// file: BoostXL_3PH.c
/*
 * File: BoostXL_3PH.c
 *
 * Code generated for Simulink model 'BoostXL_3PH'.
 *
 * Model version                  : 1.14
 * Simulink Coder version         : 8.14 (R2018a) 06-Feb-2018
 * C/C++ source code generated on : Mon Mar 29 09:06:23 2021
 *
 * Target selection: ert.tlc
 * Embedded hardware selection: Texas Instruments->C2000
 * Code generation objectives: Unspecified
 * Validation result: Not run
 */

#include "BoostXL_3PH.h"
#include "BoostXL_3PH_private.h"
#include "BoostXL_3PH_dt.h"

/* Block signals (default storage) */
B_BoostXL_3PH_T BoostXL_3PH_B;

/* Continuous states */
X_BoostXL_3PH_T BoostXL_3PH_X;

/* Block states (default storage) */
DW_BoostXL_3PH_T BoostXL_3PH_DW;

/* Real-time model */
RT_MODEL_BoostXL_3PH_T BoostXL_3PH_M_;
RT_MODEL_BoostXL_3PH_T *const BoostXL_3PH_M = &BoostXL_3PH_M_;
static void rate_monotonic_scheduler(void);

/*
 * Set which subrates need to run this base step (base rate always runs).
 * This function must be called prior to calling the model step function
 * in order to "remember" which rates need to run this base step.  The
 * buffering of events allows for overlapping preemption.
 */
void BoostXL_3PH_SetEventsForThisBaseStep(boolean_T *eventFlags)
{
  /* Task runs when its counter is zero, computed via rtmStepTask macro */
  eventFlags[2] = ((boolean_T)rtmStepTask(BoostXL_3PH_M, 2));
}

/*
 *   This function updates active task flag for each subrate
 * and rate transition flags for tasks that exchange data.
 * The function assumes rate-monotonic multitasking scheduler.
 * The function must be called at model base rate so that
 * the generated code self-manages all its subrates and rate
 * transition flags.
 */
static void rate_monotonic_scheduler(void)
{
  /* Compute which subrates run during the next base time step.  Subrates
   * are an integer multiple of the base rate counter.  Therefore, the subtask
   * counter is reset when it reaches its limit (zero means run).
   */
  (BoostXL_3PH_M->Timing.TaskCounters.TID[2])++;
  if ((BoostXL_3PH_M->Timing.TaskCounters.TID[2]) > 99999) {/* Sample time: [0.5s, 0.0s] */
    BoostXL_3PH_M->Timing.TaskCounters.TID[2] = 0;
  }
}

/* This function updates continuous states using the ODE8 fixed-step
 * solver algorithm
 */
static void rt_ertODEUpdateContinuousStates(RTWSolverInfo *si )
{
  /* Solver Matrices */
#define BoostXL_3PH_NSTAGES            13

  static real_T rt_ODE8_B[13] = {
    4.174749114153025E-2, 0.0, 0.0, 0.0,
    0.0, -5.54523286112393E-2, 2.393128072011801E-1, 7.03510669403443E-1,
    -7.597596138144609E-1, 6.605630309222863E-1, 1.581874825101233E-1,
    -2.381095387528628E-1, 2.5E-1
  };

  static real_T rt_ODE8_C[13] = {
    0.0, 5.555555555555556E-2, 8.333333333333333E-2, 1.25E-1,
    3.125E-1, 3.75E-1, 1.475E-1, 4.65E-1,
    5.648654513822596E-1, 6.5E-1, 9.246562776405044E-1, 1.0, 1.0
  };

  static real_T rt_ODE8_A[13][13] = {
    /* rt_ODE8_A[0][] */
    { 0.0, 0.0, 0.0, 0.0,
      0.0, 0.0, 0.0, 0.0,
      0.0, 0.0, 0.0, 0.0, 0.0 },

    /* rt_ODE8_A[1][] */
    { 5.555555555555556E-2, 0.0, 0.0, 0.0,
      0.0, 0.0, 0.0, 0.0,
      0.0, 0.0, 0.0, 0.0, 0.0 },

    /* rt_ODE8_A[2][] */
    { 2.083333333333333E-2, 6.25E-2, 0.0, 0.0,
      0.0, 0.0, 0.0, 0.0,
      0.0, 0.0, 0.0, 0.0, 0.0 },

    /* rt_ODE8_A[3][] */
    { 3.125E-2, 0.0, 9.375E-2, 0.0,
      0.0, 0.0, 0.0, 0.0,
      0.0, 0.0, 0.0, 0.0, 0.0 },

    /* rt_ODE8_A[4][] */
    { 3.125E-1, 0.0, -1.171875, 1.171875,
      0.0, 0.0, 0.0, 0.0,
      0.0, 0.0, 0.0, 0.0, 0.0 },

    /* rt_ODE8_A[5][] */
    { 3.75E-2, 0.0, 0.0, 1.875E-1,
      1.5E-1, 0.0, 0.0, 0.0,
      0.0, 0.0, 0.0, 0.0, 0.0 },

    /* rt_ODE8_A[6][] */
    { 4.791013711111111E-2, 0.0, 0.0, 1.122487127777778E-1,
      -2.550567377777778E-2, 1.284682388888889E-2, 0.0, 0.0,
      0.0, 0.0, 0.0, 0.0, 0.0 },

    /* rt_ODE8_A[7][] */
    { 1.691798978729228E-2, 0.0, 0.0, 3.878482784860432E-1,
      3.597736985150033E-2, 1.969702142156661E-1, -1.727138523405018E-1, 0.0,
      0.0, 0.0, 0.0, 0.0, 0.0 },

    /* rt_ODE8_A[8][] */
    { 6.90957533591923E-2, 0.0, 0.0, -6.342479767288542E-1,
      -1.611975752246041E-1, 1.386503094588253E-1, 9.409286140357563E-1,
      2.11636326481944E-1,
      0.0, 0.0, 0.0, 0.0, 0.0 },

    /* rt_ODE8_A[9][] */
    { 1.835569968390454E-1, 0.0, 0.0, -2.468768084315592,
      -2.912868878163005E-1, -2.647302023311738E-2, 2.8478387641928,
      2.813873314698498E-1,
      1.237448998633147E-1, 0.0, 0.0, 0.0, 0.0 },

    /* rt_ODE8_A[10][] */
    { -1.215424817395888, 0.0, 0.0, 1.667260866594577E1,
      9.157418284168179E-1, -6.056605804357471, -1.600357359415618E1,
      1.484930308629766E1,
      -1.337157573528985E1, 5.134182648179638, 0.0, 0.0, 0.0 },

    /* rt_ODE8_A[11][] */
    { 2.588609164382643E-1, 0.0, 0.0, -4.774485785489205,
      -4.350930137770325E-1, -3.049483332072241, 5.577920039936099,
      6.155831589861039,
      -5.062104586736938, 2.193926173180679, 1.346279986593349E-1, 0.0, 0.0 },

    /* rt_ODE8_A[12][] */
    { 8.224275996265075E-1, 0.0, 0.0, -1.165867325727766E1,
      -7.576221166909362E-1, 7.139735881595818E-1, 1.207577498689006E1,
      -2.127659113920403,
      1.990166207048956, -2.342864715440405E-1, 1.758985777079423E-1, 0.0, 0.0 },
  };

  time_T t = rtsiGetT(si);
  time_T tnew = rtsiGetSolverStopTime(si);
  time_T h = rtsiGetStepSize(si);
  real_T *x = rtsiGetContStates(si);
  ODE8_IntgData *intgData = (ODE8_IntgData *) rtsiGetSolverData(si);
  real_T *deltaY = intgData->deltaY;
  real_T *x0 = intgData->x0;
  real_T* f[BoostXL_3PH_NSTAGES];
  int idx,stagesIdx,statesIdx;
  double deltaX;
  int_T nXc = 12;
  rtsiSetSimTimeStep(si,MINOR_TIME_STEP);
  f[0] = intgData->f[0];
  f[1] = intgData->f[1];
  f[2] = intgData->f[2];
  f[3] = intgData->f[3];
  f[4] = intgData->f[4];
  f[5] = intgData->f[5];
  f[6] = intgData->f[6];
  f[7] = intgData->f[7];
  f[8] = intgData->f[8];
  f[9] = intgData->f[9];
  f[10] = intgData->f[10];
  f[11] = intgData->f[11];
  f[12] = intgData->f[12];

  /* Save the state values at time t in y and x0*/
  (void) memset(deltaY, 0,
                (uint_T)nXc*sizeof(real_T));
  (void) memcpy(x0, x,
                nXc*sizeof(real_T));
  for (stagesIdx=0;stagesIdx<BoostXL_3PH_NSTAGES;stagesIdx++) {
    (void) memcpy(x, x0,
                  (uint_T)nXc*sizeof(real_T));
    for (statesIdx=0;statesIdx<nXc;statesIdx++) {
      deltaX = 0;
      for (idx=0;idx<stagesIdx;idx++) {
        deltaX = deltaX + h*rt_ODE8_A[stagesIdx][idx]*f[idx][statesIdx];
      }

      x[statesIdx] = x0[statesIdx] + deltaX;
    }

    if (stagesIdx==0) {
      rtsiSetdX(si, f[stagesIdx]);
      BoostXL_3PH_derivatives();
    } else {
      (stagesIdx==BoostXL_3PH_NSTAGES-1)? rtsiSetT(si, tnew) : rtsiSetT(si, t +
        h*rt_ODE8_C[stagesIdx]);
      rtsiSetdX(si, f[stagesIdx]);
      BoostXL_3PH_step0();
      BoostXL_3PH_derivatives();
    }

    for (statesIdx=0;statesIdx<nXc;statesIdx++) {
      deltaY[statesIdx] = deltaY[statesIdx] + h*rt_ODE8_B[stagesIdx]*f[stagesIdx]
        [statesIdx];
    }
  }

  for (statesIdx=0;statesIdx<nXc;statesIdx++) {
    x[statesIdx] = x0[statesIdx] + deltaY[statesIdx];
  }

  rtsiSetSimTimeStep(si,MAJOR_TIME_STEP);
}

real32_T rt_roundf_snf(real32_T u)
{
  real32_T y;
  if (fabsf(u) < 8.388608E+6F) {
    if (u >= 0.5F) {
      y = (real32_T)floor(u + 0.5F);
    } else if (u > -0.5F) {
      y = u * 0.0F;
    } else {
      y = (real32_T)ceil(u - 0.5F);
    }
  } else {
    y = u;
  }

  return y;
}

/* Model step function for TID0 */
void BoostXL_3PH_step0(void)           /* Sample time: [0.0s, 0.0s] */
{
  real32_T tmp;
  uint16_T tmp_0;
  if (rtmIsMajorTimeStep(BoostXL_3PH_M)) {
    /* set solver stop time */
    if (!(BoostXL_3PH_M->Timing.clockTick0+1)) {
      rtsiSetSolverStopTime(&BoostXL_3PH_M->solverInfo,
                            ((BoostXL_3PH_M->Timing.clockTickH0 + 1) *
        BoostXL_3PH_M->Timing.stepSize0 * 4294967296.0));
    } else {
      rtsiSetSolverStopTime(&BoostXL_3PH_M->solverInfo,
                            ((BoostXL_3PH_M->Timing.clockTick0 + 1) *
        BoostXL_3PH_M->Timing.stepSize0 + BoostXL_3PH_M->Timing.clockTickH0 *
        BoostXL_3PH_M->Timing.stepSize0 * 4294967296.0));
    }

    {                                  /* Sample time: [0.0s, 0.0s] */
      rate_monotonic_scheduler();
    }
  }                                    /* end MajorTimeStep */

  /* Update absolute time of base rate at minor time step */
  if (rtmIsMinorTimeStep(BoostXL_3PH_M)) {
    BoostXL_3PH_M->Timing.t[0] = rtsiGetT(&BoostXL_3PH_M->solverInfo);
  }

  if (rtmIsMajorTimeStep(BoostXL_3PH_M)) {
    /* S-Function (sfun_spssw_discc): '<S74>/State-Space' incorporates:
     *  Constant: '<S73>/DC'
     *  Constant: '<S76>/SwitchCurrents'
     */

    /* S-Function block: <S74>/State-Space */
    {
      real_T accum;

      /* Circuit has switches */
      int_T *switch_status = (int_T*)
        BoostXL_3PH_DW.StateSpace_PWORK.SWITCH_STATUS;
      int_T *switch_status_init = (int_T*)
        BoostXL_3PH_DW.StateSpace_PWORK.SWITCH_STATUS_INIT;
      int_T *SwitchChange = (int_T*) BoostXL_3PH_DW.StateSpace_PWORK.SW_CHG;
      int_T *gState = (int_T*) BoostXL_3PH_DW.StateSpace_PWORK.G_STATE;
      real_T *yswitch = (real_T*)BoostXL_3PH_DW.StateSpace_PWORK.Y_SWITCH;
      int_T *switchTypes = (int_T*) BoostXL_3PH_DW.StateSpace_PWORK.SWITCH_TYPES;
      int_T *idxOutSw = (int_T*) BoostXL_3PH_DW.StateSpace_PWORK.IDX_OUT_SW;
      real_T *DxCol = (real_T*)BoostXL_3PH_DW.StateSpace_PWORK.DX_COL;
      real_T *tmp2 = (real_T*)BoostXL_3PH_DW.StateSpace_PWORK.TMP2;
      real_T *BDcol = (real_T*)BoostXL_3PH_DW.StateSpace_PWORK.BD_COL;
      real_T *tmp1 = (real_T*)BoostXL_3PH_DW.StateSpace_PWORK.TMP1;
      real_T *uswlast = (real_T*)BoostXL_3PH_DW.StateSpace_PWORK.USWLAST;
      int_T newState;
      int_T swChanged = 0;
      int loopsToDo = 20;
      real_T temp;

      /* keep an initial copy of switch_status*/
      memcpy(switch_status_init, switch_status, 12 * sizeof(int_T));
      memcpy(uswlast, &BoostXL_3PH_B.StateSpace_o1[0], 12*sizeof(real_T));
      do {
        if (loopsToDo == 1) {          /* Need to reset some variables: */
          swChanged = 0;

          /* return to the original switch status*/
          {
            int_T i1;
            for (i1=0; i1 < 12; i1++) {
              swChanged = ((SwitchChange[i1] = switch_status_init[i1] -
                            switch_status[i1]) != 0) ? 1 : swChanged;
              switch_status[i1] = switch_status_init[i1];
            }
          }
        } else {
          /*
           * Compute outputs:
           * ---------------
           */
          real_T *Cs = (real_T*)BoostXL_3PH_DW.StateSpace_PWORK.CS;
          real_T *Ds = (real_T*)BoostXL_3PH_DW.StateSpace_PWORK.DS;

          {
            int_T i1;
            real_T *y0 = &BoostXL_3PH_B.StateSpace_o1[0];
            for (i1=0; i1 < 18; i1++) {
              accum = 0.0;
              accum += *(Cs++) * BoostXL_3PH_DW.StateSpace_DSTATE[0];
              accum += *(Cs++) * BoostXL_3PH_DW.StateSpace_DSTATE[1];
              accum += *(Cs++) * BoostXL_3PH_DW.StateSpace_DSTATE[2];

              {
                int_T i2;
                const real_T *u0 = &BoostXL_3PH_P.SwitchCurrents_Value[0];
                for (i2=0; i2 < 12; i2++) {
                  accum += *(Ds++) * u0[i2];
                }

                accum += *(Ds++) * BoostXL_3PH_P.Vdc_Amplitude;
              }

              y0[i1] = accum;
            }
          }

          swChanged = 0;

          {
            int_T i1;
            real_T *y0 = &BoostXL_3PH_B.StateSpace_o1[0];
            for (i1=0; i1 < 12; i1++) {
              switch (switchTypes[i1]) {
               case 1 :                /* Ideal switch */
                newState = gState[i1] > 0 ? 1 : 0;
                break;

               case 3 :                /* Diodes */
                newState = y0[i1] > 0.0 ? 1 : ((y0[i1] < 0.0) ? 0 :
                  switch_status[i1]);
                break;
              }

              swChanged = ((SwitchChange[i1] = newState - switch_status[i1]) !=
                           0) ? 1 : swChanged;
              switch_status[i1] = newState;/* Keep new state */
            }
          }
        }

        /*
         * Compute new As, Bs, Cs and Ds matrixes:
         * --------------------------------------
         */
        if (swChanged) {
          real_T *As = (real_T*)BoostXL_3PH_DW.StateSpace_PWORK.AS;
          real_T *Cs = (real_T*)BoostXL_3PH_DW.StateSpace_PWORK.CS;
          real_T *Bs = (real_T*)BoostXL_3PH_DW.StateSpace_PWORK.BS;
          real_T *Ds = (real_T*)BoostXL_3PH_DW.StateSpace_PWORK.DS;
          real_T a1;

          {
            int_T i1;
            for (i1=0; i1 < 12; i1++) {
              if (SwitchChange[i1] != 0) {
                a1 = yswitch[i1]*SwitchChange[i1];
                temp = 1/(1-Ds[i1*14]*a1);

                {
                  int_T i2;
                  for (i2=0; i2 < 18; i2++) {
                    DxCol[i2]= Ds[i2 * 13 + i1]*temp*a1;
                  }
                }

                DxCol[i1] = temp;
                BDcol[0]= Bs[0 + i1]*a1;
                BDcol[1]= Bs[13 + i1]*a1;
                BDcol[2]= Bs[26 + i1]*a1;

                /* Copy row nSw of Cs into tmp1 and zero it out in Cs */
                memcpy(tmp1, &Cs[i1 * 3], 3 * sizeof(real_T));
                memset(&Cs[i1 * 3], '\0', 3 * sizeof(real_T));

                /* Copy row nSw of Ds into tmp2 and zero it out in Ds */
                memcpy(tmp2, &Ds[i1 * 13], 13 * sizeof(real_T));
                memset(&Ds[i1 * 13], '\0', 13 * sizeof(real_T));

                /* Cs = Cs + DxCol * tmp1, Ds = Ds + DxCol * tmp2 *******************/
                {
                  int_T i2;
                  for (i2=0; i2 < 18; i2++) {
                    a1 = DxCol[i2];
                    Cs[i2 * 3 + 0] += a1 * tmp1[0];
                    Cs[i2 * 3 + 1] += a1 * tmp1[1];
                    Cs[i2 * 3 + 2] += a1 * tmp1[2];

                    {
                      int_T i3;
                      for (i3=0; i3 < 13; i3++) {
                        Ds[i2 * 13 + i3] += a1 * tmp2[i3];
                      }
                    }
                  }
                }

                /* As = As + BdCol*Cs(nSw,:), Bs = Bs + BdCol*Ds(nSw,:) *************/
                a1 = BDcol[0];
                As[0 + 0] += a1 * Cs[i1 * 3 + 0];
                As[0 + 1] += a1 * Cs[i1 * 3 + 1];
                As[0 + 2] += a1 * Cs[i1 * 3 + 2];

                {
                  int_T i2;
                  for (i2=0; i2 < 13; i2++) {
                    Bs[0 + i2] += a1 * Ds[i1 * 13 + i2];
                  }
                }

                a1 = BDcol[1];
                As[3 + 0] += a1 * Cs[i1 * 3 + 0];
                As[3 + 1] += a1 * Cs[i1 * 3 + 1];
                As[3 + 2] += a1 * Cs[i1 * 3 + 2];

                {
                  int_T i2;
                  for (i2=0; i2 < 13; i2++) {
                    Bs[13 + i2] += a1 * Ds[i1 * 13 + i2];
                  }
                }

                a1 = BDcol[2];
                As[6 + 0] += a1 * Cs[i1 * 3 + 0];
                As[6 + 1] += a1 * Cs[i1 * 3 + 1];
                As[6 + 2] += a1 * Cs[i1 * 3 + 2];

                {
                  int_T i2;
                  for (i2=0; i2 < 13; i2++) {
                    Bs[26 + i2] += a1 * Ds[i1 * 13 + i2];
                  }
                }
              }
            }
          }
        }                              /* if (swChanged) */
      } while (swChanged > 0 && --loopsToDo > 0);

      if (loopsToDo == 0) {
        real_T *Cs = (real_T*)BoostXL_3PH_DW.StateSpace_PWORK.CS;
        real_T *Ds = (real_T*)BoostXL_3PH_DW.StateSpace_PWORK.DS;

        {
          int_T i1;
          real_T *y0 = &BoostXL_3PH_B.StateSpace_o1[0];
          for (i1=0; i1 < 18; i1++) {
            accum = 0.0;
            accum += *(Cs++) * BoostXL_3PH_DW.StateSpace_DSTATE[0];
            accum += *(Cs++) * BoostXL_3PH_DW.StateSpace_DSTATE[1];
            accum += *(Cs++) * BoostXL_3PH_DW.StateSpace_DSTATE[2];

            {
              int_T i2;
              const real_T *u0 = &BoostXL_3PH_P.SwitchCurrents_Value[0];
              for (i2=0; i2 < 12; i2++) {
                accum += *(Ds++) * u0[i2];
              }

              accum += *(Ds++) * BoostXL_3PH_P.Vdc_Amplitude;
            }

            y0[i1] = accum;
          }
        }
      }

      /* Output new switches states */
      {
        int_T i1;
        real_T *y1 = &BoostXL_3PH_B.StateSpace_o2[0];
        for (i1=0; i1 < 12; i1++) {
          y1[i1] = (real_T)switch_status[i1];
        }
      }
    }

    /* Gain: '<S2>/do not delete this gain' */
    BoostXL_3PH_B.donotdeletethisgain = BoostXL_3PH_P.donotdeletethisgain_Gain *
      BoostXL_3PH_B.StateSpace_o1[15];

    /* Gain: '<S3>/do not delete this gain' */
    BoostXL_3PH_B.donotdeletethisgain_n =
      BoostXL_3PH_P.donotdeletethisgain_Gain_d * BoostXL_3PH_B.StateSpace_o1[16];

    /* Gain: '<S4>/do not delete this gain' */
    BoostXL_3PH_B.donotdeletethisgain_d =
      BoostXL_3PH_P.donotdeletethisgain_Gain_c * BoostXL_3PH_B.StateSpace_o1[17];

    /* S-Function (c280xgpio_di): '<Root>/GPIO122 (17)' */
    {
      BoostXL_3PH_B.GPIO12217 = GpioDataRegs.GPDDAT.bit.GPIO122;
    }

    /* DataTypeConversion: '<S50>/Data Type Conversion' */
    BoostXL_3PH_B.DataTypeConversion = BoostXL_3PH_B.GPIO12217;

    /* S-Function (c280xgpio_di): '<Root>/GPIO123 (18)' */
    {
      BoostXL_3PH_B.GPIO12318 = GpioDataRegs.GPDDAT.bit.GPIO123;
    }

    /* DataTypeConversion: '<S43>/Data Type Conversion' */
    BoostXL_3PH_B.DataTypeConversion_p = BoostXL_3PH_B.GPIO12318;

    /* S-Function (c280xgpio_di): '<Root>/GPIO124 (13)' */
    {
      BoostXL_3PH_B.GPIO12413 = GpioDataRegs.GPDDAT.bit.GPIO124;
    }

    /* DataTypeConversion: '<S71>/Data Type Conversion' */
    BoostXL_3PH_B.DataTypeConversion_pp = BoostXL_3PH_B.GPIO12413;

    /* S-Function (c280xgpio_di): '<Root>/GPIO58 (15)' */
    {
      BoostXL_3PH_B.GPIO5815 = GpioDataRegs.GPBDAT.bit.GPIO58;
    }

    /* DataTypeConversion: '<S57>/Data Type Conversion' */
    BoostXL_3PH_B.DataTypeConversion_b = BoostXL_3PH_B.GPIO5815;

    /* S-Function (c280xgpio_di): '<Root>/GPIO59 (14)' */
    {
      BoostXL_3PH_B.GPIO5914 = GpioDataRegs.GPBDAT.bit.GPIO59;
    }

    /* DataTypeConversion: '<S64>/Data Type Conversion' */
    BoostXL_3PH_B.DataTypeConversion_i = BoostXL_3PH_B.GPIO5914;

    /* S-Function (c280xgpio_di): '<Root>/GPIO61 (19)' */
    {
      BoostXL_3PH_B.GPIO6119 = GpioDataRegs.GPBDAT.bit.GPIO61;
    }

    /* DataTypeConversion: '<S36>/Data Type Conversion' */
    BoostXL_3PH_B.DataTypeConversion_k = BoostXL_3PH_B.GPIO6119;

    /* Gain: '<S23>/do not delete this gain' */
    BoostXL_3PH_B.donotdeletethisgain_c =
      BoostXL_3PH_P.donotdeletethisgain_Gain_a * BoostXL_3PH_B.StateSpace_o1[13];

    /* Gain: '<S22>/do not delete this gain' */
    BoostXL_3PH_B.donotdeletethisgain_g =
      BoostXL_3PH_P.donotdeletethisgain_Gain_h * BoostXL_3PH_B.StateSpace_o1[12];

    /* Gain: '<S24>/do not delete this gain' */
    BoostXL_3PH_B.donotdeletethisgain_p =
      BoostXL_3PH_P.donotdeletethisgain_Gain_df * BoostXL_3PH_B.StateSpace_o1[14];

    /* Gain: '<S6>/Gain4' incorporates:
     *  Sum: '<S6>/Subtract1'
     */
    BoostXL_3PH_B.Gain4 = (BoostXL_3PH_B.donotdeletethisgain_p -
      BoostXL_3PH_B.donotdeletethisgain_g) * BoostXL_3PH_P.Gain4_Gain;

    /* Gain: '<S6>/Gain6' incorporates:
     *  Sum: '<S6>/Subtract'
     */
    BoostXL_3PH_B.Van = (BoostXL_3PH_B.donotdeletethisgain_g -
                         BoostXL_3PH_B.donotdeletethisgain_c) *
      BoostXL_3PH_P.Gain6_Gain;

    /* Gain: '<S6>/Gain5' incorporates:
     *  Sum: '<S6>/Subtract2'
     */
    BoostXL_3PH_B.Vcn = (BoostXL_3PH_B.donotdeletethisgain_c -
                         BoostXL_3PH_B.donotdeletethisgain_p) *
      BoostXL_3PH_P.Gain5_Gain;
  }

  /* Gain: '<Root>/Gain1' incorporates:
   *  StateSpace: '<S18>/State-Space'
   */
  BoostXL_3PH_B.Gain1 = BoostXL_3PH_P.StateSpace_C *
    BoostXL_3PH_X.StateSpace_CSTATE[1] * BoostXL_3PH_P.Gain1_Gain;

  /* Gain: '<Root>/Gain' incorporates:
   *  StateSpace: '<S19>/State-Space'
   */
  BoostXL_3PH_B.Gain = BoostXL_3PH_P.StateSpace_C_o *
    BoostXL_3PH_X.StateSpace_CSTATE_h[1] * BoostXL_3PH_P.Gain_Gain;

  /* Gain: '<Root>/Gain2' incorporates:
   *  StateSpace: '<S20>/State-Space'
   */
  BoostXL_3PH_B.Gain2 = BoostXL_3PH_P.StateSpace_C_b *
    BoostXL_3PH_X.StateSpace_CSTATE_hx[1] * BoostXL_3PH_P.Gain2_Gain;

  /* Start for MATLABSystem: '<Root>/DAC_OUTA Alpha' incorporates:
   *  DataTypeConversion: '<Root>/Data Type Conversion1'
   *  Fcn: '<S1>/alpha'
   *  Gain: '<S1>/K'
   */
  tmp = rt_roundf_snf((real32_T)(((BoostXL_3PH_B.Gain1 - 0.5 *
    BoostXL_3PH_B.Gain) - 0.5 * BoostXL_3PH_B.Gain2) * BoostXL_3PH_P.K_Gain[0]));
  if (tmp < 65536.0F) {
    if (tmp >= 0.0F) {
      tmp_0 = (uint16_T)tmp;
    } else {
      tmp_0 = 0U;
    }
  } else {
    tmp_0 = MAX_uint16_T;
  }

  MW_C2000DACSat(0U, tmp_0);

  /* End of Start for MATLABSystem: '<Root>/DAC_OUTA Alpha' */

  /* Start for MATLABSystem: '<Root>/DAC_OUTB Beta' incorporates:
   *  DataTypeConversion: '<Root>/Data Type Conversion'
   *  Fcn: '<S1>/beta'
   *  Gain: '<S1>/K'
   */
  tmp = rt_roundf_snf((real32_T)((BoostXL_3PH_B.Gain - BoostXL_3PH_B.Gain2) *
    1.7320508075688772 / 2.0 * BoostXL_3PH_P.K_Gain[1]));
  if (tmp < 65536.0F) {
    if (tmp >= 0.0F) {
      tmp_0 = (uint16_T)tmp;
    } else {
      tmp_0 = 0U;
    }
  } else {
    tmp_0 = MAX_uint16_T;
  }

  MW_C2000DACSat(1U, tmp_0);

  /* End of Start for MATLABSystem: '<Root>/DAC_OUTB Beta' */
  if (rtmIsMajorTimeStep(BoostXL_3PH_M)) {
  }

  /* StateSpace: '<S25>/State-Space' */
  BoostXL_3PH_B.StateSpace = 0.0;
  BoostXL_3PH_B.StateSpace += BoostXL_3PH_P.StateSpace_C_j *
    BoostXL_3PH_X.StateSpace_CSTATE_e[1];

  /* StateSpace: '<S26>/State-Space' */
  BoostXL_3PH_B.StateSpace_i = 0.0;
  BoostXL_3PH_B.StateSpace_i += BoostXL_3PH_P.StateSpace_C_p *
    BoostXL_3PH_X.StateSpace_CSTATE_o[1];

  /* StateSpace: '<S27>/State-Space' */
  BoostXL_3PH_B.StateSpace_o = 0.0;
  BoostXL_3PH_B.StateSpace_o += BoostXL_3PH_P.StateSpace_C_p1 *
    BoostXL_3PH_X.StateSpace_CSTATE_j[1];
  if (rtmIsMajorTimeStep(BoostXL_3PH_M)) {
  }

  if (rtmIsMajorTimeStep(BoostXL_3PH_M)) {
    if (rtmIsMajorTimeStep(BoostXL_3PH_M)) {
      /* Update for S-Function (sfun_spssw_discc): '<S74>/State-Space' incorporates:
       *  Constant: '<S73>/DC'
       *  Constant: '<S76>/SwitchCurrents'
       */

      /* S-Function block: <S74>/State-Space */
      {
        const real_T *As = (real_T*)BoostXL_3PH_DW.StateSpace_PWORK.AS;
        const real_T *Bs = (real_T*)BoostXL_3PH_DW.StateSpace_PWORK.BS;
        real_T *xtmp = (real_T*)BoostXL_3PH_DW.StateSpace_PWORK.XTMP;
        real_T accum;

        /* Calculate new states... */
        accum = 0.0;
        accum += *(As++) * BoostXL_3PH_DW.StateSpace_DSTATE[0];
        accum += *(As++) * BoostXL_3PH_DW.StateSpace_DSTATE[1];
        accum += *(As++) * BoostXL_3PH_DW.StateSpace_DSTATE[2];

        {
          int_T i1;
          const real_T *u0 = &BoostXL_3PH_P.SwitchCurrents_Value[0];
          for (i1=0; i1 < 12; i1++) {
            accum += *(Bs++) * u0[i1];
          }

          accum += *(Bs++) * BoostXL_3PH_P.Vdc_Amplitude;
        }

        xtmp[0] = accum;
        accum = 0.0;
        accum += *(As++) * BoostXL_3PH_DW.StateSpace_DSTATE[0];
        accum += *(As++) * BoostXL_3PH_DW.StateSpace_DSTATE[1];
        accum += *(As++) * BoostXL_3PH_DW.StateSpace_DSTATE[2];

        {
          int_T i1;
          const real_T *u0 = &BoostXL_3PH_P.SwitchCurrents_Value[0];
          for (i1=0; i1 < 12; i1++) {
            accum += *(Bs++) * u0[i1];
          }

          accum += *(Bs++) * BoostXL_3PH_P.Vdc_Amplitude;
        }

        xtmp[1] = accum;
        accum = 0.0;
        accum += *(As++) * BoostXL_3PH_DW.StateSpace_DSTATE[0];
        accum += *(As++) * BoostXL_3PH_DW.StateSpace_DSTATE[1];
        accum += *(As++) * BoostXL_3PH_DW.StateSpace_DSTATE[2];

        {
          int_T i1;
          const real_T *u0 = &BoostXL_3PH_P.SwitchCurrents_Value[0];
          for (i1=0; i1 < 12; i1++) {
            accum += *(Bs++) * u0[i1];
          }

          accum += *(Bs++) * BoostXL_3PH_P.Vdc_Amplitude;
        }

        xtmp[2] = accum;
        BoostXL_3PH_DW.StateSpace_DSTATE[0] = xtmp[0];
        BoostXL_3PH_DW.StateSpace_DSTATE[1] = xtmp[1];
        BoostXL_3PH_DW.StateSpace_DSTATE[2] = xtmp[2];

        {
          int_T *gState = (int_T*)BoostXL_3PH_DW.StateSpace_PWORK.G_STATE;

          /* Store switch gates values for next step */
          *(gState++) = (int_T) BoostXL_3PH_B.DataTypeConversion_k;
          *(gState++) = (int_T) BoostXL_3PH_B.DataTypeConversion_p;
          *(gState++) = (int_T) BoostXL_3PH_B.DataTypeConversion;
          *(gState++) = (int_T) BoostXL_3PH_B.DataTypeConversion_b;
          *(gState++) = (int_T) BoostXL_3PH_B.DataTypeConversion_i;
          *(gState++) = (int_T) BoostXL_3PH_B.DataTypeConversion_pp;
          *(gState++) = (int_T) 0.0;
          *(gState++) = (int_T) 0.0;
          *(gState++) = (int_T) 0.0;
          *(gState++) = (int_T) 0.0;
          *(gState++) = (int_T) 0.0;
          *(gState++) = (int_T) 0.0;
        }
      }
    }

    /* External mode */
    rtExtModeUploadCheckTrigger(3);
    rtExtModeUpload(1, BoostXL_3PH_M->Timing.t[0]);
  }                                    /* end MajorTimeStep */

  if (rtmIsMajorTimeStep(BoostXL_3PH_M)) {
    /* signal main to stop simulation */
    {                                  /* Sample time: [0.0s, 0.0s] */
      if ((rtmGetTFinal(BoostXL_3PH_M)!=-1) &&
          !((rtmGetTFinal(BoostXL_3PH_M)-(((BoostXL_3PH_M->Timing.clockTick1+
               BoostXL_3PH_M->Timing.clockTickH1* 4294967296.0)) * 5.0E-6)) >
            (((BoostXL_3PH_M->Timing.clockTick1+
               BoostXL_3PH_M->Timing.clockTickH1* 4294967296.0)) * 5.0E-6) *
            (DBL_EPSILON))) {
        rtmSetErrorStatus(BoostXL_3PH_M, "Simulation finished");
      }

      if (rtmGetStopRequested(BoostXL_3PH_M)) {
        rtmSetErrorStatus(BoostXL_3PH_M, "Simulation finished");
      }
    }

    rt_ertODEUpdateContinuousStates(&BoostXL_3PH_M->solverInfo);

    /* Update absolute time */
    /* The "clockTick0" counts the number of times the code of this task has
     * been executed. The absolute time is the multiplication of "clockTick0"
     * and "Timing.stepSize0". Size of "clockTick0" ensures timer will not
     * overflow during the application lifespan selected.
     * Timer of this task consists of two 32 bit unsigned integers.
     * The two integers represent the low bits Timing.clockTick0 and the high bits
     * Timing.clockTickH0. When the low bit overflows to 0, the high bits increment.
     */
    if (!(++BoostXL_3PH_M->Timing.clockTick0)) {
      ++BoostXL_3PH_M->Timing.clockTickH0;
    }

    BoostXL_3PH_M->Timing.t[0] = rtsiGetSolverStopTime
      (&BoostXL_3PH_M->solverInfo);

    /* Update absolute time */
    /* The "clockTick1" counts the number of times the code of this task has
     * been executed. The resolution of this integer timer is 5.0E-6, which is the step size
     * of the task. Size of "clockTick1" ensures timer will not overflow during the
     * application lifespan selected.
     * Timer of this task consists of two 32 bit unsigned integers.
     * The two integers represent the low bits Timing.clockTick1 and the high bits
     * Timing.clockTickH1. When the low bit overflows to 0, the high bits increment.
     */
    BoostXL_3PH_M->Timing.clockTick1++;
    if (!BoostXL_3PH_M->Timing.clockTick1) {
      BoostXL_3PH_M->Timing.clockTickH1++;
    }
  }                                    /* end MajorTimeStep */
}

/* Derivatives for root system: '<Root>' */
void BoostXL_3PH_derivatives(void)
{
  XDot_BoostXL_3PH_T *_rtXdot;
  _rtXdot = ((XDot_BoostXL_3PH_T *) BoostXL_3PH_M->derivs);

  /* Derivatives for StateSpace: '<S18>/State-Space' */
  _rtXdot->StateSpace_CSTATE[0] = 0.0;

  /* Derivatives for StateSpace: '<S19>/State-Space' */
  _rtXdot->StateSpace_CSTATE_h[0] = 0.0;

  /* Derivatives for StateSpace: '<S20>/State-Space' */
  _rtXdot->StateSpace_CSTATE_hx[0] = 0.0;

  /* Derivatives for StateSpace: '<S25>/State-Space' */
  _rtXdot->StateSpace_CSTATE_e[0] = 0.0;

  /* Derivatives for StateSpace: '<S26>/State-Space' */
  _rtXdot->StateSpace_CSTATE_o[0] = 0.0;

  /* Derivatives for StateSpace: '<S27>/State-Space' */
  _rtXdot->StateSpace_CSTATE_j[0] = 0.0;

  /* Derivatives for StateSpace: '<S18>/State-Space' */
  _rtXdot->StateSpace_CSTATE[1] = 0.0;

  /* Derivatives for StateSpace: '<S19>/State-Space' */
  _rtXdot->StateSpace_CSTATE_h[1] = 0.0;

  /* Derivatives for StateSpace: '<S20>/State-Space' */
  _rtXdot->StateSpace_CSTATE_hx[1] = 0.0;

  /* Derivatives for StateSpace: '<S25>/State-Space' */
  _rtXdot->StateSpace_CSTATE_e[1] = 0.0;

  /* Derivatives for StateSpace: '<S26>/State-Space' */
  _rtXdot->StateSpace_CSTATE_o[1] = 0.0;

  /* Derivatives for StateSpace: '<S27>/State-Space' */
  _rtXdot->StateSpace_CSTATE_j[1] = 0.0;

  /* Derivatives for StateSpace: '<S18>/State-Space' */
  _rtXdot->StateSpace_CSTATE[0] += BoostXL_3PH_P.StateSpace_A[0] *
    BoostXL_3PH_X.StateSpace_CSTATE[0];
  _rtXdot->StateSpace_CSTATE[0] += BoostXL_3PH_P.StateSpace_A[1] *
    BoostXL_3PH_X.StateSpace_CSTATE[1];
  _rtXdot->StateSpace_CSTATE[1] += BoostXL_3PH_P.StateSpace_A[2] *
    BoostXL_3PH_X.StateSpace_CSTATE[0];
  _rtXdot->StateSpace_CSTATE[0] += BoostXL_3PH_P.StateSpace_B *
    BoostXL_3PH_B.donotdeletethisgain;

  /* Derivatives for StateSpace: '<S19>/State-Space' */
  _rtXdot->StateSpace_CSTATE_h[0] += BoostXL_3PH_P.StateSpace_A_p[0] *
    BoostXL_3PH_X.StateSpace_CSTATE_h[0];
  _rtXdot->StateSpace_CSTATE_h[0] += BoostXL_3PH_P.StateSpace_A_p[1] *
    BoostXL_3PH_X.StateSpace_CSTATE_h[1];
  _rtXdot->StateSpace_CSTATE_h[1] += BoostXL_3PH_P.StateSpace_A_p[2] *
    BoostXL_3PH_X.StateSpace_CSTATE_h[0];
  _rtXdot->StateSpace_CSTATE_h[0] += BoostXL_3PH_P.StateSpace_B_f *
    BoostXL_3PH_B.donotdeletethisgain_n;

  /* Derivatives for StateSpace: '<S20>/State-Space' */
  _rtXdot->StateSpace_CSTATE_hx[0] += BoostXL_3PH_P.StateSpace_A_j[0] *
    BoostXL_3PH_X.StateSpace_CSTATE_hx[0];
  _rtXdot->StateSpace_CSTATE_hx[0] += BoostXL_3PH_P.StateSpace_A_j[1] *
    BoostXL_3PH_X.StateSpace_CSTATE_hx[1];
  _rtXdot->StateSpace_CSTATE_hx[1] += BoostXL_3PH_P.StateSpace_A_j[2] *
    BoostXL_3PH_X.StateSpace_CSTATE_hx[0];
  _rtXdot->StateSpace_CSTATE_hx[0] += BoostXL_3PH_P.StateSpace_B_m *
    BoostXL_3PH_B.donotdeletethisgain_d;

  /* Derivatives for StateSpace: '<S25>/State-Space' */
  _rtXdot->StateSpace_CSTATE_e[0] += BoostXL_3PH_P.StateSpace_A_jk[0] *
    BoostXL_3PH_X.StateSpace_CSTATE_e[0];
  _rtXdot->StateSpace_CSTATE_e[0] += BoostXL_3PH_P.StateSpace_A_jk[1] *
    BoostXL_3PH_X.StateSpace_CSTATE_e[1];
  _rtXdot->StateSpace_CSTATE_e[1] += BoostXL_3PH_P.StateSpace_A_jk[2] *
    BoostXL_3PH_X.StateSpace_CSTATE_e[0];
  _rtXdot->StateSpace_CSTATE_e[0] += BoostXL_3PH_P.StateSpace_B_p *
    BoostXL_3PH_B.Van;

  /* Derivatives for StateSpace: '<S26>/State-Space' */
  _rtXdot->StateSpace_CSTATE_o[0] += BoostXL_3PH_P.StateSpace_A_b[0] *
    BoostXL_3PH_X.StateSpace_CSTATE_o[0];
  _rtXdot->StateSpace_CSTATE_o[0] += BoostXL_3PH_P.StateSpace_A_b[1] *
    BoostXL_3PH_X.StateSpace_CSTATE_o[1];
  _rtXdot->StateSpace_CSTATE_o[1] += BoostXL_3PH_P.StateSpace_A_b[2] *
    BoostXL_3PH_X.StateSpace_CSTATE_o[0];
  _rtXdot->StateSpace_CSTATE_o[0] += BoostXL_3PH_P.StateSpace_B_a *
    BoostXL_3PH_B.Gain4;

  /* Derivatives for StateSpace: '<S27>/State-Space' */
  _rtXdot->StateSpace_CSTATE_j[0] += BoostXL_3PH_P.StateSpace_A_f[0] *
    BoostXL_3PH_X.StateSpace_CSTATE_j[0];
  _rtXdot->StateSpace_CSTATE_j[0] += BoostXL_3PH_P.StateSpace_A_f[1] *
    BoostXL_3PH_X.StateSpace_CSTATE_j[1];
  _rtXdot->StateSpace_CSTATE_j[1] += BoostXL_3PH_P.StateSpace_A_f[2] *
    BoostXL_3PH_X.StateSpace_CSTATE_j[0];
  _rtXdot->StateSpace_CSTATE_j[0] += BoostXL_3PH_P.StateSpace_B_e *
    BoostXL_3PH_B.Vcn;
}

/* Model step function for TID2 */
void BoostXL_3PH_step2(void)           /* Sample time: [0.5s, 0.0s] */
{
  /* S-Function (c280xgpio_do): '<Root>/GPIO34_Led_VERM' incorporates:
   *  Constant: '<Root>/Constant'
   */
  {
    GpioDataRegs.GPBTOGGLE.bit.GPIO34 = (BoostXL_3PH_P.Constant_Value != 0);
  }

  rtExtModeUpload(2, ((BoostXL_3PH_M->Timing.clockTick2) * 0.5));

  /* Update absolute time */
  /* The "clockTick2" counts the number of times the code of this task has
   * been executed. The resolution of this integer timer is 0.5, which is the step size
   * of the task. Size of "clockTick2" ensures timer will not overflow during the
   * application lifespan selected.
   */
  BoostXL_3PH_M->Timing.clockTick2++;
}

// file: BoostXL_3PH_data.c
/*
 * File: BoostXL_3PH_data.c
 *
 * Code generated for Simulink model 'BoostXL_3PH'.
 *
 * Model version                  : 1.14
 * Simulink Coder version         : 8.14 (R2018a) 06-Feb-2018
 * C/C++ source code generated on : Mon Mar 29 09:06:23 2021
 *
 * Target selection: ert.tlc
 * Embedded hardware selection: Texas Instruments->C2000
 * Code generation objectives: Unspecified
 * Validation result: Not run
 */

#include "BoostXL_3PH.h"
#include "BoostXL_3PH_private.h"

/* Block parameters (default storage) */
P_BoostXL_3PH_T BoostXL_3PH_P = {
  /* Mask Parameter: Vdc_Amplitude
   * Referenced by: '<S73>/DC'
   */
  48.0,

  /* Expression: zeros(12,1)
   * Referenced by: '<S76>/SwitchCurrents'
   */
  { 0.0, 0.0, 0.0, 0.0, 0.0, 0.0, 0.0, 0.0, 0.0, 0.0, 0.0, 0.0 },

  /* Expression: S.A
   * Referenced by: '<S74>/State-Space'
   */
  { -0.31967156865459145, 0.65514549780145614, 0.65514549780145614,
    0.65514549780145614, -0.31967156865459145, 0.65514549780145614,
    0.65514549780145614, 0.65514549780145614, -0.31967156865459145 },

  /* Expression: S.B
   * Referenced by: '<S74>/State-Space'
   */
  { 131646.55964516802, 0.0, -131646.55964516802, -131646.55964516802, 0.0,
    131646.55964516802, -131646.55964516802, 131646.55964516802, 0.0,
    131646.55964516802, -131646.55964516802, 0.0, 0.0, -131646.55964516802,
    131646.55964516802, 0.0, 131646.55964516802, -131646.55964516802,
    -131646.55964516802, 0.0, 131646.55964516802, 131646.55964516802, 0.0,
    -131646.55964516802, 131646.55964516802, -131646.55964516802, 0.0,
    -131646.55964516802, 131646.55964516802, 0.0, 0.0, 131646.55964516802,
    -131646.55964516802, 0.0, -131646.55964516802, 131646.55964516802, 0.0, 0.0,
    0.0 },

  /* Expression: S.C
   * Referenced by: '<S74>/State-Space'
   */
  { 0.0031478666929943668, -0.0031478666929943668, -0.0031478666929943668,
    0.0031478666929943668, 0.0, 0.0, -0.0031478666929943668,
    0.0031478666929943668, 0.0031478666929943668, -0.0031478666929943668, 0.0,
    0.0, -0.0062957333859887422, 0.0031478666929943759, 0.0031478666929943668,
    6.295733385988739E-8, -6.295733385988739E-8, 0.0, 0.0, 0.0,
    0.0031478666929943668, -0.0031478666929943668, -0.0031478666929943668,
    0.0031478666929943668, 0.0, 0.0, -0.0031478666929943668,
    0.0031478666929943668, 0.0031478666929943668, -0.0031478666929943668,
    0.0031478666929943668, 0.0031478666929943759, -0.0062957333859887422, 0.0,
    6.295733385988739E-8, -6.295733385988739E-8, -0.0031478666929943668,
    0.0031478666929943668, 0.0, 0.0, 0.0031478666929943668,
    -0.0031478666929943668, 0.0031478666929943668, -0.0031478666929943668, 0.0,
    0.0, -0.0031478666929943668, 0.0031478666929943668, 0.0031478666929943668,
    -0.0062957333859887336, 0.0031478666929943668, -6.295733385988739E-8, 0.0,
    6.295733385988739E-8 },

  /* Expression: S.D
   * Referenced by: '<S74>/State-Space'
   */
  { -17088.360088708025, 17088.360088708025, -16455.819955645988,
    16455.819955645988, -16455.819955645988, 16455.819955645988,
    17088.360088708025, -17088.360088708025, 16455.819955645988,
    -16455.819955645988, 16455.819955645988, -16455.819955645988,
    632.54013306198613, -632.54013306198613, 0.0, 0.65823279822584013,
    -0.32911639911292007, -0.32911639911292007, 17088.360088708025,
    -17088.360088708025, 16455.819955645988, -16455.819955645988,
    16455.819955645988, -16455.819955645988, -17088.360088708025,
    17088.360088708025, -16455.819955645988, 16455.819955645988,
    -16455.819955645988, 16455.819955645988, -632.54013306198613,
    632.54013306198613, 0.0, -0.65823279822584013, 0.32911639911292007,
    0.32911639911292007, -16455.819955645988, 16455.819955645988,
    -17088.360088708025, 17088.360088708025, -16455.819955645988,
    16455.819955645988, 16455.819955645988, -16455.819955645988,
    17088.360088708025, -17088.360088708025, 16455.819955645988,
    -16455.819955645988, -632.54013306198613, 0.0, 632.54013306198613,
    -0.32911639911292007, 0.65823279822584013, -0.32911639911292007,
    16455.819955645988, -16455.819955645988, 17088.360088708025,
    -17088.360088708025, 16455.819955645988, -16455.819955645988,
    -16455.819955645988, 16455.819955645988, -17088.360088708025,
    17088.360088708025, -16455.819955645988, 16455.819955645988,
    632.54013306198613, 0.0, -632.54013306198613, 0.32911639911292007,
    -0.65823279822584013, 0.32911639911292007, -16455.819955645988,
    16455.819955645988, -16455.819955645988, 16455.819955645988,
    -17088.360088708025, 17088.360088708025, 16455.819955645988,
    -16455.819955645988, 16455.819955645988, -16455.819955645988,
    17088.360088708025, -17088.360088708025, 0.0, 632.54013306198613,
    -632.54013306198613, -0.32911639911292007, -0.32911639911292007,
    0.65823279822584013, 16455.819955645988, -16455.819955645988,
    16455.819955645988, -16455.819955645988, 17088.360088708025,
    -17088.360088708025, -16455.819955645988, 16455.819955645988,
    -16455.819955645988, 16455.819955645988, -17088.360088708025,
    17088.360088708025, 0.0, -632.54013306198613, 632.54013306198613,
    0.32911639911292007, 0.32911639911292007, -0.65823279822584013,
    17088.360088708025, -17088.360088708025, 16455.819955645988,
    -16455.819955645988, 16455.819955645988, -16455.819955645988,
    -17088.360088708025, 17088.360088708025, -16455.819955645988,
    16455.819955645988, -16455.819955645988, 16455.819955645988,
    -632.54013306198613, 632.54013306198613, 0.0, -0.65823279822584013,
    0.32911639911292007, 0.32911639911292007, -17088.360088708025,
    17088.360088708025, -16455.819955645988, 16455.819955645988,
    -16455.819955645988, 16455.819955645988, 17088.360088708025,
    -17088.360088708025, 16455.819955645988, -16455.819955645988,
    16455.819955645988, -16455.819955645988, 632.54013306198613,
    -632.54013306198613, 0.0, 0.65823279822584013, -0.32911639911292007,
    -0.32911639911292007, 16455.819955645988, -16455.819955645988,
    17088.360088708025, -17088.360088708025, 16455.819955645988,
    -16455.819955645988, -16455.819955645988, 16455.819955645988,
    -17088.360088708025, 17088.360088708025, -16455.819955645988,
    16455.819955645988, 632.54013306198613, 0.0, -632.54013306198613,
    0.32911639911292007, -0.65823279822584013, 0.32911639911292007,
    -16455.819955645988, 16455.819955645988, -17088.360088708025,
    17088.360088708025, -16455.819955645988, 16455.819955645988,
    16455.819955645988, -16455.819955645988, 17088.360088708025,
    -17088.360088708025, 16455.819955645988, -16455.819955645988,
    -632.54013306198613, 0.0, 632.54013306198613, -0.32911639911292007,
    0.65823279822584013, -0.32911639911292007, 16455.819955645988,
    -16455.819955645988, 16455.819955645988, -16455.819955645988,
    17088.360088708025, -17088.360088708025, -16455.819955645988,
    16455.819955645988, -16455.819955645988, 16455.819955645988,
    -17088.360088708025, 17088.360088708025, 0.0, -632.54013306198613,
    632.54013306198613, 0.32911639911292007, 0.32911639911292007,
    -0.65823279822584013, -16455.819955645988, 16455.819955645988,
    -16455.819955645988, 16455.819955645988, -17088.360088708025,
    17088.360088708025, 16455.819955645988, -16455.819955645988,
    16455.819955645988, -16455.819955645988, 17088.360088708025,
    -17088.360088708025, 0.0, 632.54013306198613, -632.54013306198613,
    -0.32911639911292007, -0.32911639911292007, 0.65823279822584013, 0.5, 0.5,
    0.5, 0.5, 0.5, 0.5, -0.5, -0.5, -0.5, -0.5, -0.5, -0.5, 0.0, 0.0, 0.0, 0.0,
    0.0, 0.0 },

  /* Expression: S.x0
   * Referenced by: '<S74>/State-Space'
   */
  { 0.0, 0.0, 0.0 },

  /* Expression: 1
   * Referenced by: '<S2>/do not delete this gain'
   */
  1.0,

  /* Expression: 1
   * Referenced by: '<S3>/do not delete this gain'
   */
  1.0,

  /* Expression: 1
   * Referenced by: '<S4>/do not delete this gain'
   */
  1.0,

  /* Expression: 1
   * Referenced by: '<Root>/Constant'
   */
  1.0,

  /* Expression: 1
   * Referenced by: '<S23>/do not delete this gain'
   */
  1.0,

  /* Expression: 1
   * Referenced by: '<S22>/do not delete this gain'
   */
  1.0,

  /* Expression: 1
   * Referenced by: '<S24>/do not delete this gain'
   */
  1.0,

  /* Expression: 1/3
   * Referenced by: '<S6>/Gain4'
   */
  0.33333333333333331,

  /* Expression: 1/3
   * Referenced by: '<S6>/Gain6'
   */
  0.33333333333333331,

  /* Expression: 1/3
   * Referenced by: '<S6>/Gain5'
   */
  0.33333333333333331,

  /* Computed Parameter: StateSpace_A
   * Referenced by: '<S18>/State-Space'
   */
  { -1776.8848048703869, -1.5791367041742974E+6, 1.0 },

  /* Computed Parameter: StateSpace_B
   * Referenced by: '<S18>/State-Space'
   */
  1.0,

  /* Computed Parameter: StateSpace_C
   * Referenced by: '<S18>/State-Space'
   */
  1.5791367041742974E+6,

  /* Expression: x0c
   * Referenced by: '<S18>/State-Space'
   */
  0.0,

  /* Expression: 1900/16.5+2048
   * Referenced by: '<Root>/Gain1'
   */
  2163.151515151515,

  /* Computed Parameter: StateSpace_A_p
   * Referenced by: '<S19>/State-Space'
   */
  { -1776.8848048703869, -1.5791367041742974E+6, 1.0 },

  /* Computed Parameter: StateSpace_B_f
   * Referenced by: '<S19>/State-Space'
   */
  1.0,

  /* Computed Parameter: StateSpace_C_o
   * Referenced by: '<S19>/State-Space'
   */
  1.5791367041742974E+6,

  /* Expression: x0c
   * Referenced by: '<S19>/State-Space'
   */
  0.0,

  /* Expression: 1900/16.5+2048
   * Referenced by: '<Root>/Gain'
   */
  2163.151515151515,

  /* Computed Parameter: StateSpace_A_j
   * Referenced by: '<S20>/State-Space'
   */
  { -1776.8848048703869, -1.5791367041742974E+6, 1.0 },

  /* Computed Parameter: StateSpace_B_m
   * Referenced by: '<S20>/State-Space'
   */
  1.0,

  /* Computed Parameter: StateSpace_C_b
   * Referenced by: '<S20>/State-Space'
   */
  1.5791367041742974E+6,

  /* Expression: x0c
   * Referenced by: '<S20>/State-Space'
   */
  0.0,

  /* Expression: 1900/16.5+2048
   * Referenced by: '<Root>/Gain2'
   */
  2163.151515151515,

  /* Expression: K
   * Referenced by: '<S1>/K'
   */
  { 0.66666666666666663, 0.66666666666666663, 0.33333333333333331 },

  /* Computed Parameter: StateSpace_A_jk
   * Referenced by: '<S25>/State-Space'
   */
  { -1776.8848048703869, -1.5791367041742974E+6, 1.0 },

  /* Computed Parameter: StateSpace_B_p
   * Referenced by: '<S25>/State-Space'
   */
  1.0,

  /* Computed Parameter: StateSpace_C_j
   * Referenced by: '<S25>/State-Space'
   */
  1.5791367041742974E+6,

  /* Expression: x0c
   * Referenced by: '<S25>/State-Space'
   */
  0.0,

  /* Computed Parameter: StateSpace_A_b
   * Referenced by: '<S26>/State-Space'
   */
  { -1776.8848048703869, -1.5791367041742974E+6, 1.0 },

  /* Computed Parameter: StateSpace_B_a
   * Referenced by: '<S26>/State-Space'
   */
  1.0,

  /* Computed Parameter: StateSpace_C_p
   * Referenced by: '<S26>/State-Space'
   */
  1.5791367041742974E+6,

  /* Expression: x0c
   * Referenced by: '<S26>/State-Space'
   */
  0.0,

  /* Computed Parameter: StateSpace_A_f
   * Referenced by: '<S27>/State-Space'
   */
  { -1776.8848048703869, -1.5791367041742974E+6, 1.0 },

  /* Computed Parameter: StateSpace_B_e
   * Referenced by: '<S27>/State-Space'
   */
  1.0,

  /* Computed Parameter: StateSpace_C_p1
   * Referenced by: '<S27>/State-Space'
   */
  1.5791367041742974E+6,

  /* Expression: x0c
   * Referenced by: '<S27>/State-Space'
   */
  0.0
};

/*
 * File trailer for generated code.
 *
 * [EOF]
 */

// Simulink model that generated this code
simulink model "BoostXL_3PH"  (R2018a)
settings: Solver=ode8  StartTime=0.0  StopTime=Inf  FixedStep=5e-6  MaxStep=5e-6  RelTol=1e-3  EnableMultiTasking=on
libraries: powerlib x15, c2837xDlib x9, powerlib_extras x6, peTransforms x1

== system BoostXL_3PH ==
  note: CONVERSOR TRIFÁSICO BOOSTXL
      | Victor Lopes
  Clarke Transform : peTransforms/Clarke Transform  PowerInvariant=off
  Constant : Constant  SampleTime=0.5
  Current Measueent1 : powerlib/Measurements/Current Measurement  PhasorSimulation=off  OutputType=Magnitude  PSBequivalent=0
  Current Measueent2 : powerlib/Measurements/Current Measurement  PhasorSimulation=off  OutputType=Magnitude  PSBequivalent=0
  Current Measueent3 : powerlib/Measurements/Current Measurement  PhasorSimulation=off  OutputType=Magnitude  PSBequivalent=0
  DAC_OUTA Alpha : c2837xDlib/DAC  channel=A  saturate=on
  DAC_OUTB Beta : c2837xDlib/DAC  channel=B  saturate=on
  Data Type Conversion : DataTypeConversion
  Data Type Conversion1 : DataTypeConversion
  Demux : Demux  Outputs=3
  GPIO122 (17) : c2837xDlib/Digital Input  GPIO_Number=GPIO120~GPIO127  GPIO_Bit0=off  GPIO_Bit1=off  GPIO_Bit2=on  GPIO_Bit3=off  GPIO_Bit4=off  GPIO_Bit5=off  GPIO_Bit6=off  GPIO_Bit7=off  sampleTime=-1  dataType=boolean  GPIO_Bit0_Qualification=Sync to SYSCLKOUT  GPIO_Bit1_Qualification=Sync to SYSCLKOUT  GPIO_Bit2_Qualification=Sync to SYSCLKOUT  GPIO_Bit3_Qualification=Sync to SYSCLKOUT  GPIO_Bit4_Qualification=Sync to SYSCLKOUT  GPIO_Bit5_Qualification=Sync to SYSCLKOUT  GPIO_Bit6_Qualification=Sync to SYSCLKOUT  GPIO_Bit7_Qualification=Sync to SYSCLKOUT  Qualification_Period=-1
  GPIO123 (18) : c2837xDlib/Digital Input  GPIO_Number=GPIO120~GPIO127  GPIO_Bit0=off  GPIO_Bit1=off  GPIO_Bit2=off  GPIO_Bit3=on  GPIO_Bit4=off  GPIO_Bit5=off  GPIO_Bit6=off  GPIO_Bit7=off  sampleTime=-1  dataType=boolean  GPIO_Bit0_Qualification=Sync to SYSCLKOUT  GPIO_Bit1_Qualification=Sync to SYSCLKOUT  GPIO_Bit2_Qualification=Sync to SYSCLKOUT  GPIO_Bit3_Qualification=Sync to SYSCLKOUT  GPIO_Bit4_Qualification=Sync to SYSCLKOUT  GPIO_Bit5_Qualification=Sync to SYSCLKOUT  GPIO_Bit6_Qualification=Sync to SYSCLKOUT  GPIO_Bit7_Qualification=Sync to SYSCLKOUT  Qualification_Period=-1
  GPIO124 (13) : c2837xDlib/Digital Input  GPIO_Number=GPIO120~GPIO127  GPIO_Bit0=off  GPIO_Bit1=off  GPIO_Bit2=off  GPIO_Bit3=off  GPIO_Bit4=on  GPIO_Bit5=off  GPIO_Bit6=off  GPIO_Bit7=off  sampleTime=-1  dataType=boolean  GPIO_Bit0_Qualification=Sync to SYSCLKOUT  GPIO_Bit1_Qualification=Sync to SYSCLKOUT  GPIO_Bit2_Qualification=Sync to SYSCLKOUT  GPIO_Bit3_Qualification=Sync to SYSCLKOUT  GPIO_Bit4_Qualification=Sync to SYSCLKOUT  GPIO_Bit5_Qualification=Sync to SYSCLKOUT  GPIO_Bit6_Qualification=Sync to SYSCLKOUT  GPIO_Bit7_Qualification=Sync to SYSCLKOUT  Qualification_Period=-1
  GPIO34_Led_VERM : c2837xDlib/Digital Output  GPIO_Number=GPIO32~GPIO39  GPIO_Bit0=off  GPIO_BIT0_Toggle=off  GPIO_Bit1=off  GPIO_BIT1_Toggle=off  GPIO_Bit2=on  GPIO_BIT2_Toggle=on  GPIO_Bit3=off  GPIO_BIT3_Toggle=off  GPIO_Bit4=off  GPIO_BIT4_Toggle=off  GPIO_Bit5=off  GPIO_BIT5_Toggle=off  GPIO_Bit6=off  GPIO_BIT6_Toggle=off  GPIO_Bit7=off  GPIO_BIT7_Toggle=off
  GPIO58 (15) : c2837xDlib/Digital Input  GPIO_Number=GPIO56~GPIO63  GPIO_Bit0=off  GPIO_Bit1=off  GPIO_Bit2=on  GPIO_Bit3=off  GPIO_Bit4=off  GPIO_Bit5=off  GPIO_Bit6=off  GPIO_Bit7=off  sampleTime=-1  dataType=boolean  GPIO_Bit0_Qualification=Sync to SYSCLKOUT  GPIO_Bit1_Qualification=Sync to SYSCLKOUT  GPIO_Bit2_Qualification=Sync to SYSCLKOUT  GPIO_Bit3_Qualification=Sync to SYSCLKOUT  GPIO_Bit4_Qualification=Sync to SYSCLKOUT  GPIO_Bit5_Qualification=Sync to SYSCLKOUT  GPIO_Bit6_Qualification=Sync to SYSCLKOUT  GPIO_Bit7_Qualification=Sync to SYSCLKOUT  Qualification_Period=-1
  GPIO59 (14) : c2837xDlib/Digital Input  GPIO_Number=GPIO56~GPIO63  GPIO_Bit0=off  GPIO_Bit1=off  GPIO_Bit2=off  GPIO_Bit3=on  GPIO_Bit4=off  GPIO_Bit5=off  GPIO_Bit6=off  GPIO_Bit7=off  sampleTime=-1  dataType=boolean  GPIO_Bit0_Qualification=Sync to SYSCLKOUT  GPIO_Bit1_Qualification=Sync to SYSCLKOUT  GPIO_Bit2_Qualification=Sync to SYSCLKOUT  GPIO_Bit3_Qualification=Sync to SYSCLKOUT  GPIO_Bit4_Qualification=Sync to SYSCLKOUT  GPIO_Bit5_Qualification=Sync to SYSCLKOUT  GPIO_Bit6_Qualification=Sync to SYSCLKOUT  GPIO_Bit7_Qualification=Sync to SYSCLKOUT  Qualification_Period=-1
  GPIO61 (19) : c2837xDlib/Digital Input  GPIO_Number=GPIO56~GPIO63  GPIO_Bit0=off  GPIO_Bit1=off  GPIO_Bit2=off  GPIO_Bit3=off  GPIO_Bit4=off  GPIO_Bit5=on  GPIO_Bit6=off  GPIO_Bit7=off  sampleTime=-1  dataType=boolean  GPIO_Bit0_Qualification=Sync to SYSCLKOUT  GPIO_Bit1_Qualification=Sync to SYSCLKOUT  GPIO_Bit2_Qualification=Sync to SYSCLKOUT  GPIO_Bit3_Qualification=Sync to SYSCLKOUT  GPIO_Bit4_Qualification=Sync to SYSCLKOUT  GPIO_Bit5_Qualification=Sync to SYSCLKOUT  GPIO_Bit6_Qualification=Sync to SYSCLKOUT  GPIO_Bit7_Qualification=Sync to SYSCLKOUT  Qualification_Period=-1
  Gain : Gain  Gain=1900/16.5+2048
  Gain1 : Gain  Gain=1900/16.5+2048
  Gain2 : Gain  Gain=1900/16.5+2048
  LP filter 2nd order : Subsystem  mask{cutoff_frequency=200, damping_factor=0.707}
      mask prompts: cutoff_frequency "Cut off frequency"; damping_factor "Damping Factor"
  Medição_Tensões : Subsystem
  Mosfet{,1..5} (6 alike) : powerlib/Power Electronics/Mosfet  Ron=0.1  Lon=0  Rd=0.01  Vfd=0  IC=0  Rs=1e5  Cs=inf  Measurements=off
  Mux : Mux  Inputs=3
  RL_load : powerlib/Elements/Three-Phase Series RLC Load  LConnTagsString=A|B|C  Configuration=Delta  NominalVoltage=25  Vabc=[1e3 1e3 1e3]  Vabcp=[1e3 1e3 1e3]  NominalFrequency=60  UnbalancedPower=off  ActivePower=200  InductivePower=40  CapacitivePower=0  Pabc=[10e3 9e3 11e3]  QLabc=[100 90 110]  QCabc=[100 90 110]  Pabcp=[10e3 9e3 11e3]  QLabcp=[100 90 110]  QCabcp=[100 90 110]  Measurements=Branch voltages and currents  LoadType=constant Z
  Scope{1,4,8,10} (4 alike) : Scope
  Terminator : Terminator
  To Workspace : ToWorkspace  VariableName=Vph  SaveFormat=Timeseries  SampleTime=-1
  To Workspace1 : ToWorkspace  VariableName=Vline  SaveFormat=Timeseries  SampleTime=-1
  To Workspace2 : ToWorkspace  VariableName=Vph_noPWM  SaveFormat=Timeseries  SampleTime=-1
  To Workspace3 : ToWorkspace  VariableName=ILoad  SaveFormat=Timeseries  SampleTime=-1
  Vdc : powerlib/Electrical Sources/DC Voltage Source  Amplitude=48  Measurements=None
  powergui : powerlib/powergui  Priority=1  SimulationMode=Discrete  SampleTime=5e-6  frequency=60  Iterations=50  frequencyindice=0  Pbase=100e6  ErrMax=1e-4  UnitsV=kV  UnitsW=MW  buscounter=0  FunctionMessages=off  echomessages=off  EnableUseOfTLC=off  CurrentSourceSwitches=off  DisableSnubberDevices=off  DisableRonSwitches=off  DisableVfSwitches=off  DisplayEquations=off  SolverType=Tustin/Backward Euler (TBE)  Interpol=off  ExternalGateDelay=off  methode=off  Ts=100  x0status=blocks  SPID=off  SwTol=0  HookPort=off  RestoreLinks=warning  ResistiveCurrentMeasurement=off  Frange=[0:2:500]  Ylog=off  Xlog=on  ShowGrid=off  save=off  variable=ZData  structure=0  ZoomFFT=off  StartTime=0.0  cycles=1  DisplayStyle=1  fundamental=60  FreqAxis=off  MaxFrequency=1000  frequencyindicesteady=1  RmsSteady=1  display=off
  wires:
  Clarke Transform/1 -> Demux/1
  Current Measueent3/1 -> LP filter 2nd order/3(c)
  LP filter 2nd order/2(B) -> Gain/1
  LP filter 2nd order/1(A) -> Gain1/1
  LP filter 2nd order/3(C) -> Gain2/1
  Current Measueent1/1 -> LP filter 2nd order/1(a)
  Gain/1 -> Mux/2
  Mux/1 -> To Workspace3/1, Clarke Transform/1, Scope1/1
  Gain2/1 -> Mux/3
  Gain1/1 -> Mux/1
  Current Measueent2/1 -> LP filter 2nd order/2(b)
  Demux/1 -> Data Type Conversion1/1
  Data Type Conversion1/1 -> DAC_OUTA Alpha/1
  Demux/2 -> Data Type Conversion/1
  Data Type Conversion/1 -> DAC_OUTB Beta/1
  Demux/3 -> Terminator/1
  Medição_Tensões/3(V_noPWM) -> To Workspace2/1, Scope10/1
  Medição_Tensões/2(Vln) -> To Workspace1/1, Scope4/1
  Medição_Tensões/1(Vph) -> To Workspace/1, Scope8/1
  GPIO61 (19)/1 -> Mosfet/1
  GPIO122 (17)/1 -> Mosfet2/1
  GPIO59 (14)/1 -> Mosfet4/1
  GPIO124 (13)/1 -> Mosfet5/1
  GPIO58 (15)/1 -> Mosfet3/1
  GPIO123 (18)/1 -> Mosfet1/1
  Constant/1 -> GPIO34_Led_VERM/1
  connections:
  Mosfet2/LConn1 -- Mosfet4/LConn1 -- Vdc/RConn1 -- Mosfet/LConn1
  Current Measueent2/RConn1 -- RL_load/LConn2 -- Medição_Tensões/LConn2
  Current Measueent1/LConn1 -- Mosfet/RConn1 -- Mosfet1/LConn1
  RL_load/LConn3 -- Medição_Tensões/LConn3 -- Current Measueent3/RConn1
  Current Measueent1/RConn1 -- RL_load/LConn1 -- Medição_Tensões/LConn1
  Current Measueent2/LConn1 -- Mosfet2/RConn1 -- Mosfet3/LConn1
  Mosfet1/RConn1 -- Vdc/LConn1 -- Mosfet5/RConn1 -- Mosfet3/RConn1
  Current Measueent3/LConn1 -- Mosfet5/LConn1 -- Mosfet4/RConn1

== system BoostXL_3PH/LP filter 2nd order ==
  a : Inport
  b : Inport  Port=2
  c : Inport  Port=3
  2nd-Order Filter : powerlib_extras/Control  Blocks/2nd-Order Filter  FilterType=Lowpass  Fo=cutoff_frequency  Zeta=damping_factor  Initialize=off  Vac_Init=[1 45 60]  Vdc_Init=-0.5  PlotResponse=off  param1=[1 500 1]
  2nd-Order Filter1 : powerlib_extras/Control  Blocks/2nd-Order Filter  FilterType=Lowpass  Fo=cutoff_frequency  Zeta=damping_factor  Initialize=off  Vac_Init=[1 45 60]  Vdc_Init=-0.5  PlotResponse=off  param1=[1 500 1]
  2nd-Order Filter2 : powerlib_extras/Control  Blocks/2nd-Order Filter  FilterType=Lowpass  Fo=cutoff_frequency  Zeta=damping_factor  Initialize=off  Vac_Init=[1 45 60]  Vdc_Init=-0.5  PlotResponse=off  param1=[1 500 1]
  A : Outport
  B : Outport  Port=2
  C : Outport  Port=3
  wires:
  a/1 -> 2nd-Order Filter/1
  2nd-Order Filter/1 -> A/1
  b/1 -> 2nd-Order Filter1/1
  2nd-Order Filter1/1 -> B/1
  c/1 -> 2nd-Order Filter2/1
  2nd-Order Filter2/1 -> C/1

== system BoostXL_3PH/Medição_Tensões ==
  Gain4 : Gain  Gain=1/3
  Gain5 : Gain  Gain=1/3
  Gain6 : Gain  Gain=1/3
  LP filter 2nd order : Subsystem  mask{cutoff_frequency=200, damping_factor=0.707}
      mask prompts: cutoff_frequency "Cut off frequency"; damping_factor "Damping Factor"
  Mux1 : Mux  Inputs=3
  Mux5 : Mux  Inputs=3
  Mux6 : Mux  Inputs=3
  Subtract : Sum  Inputs=-+
  Subtract1 : Sum  Inputs=-+
  Subtract2 : Sum  Inputs=+-
  Voltage Measurement1 : powerlib/Measurements/Voltage Measurement  PhasorSimulation=off  OutputType=Complex  PSBequivalent=0
  Voltage Measurement2 : powerlib/Measurements/Voltage Measurement  PhasorSimulation=off  OutputType=Complex  PSBequivalent=0
  Voltage Measurement3 : powerlib/Measurements/Voltage Measurement  PhasorSimulation=off  OutputType=Complex  PSBequivalent=0
  Va : PMIOPort  Side=Left
  Vb : PMIOPort  Port=2  Side=Left
  Vc : PMIOPort  Port=3  Side=Left
  Vph : Outport
  Vln : Outport  Port=2
  V_noPWM : Outport  Port=3
  wires:
  Gain4/1 -> LP filter 2nd order/2(b), Mux5/2
  Voltage Measurement3/1 -> Subtract1/2, Subtract2/2, Mux1/3
  Voltage Measurement1/1 -> Subtract/2, Subtract1/1, Mux1/2
  Gain6/1 -> LP filter 2nd order/1(a), Mux5/1  "Van"
  LP filter 2nd order/2(B) -> Mux6/2
  Subtract2/1 -> Gain5/1
  Voltage Measurement2/1 -> Subtract2/1, Subtract/1, Mux1/1
  Gain5/1 -> LP filter 2nd order/3(c), Mux5/3  "Vcn"
  LP filter 2nd order/1(A) -> Mux6/1
  Mux5/1 -> Vph/1
  Subtract/1 -> Gain6/1
  Subtract1/1 -> Gain4/1
  LP filter 2nd order/3(C) -> Mux6/3
  Mux1/1 -> Vln/1
  Mux6/1 -> V_noPWM/1
  connections:
  Voltage Measurement2/LConn1 -- Vc/RConn1 -- Voltage Measurement3/LConn2
  Voltage Measurement1/LConn1 -- Va/RConn1 -- Voltage Measurement2/LConn2
  Voltage Measurement3/LConn1 -- Vb/RConn1 -- Voltage Measurement1/LConn2

== system BoostXL_3PH/Medição_Tensões/LP filter 2nd order ==
  a : Inport
  b : Inport  Port=2
  c : Inport  Port=3
  2nd-Order Filter : powerlib_extras/Control  Blocks/2nd-Order Filter  FilterType=Lowpass  Fo=cutoff_frequency  Zeta=damping_factor  Initialize=off  Vac_Init=[1 45 60]  Vdc_Init=-0.5  PlotResponse=off  param1=[1 500 1]
  2nd-Order Filter1 : powerlib_extras/Control  Blocks/2nd-Order Filter  FilterType=Lowpass  Fo=cutoff_frequency  Zeta=damping_factor  Initialize=off  Vac_Init=[1 45 60]  Vdc_Init=-0.5  PlotResponse=off  param1=[1 500 1]
  2nd-Order Filter2 : powerlib_extras/Control  Blocks/2nd-Order Filter  FilterType=Lowpass  Fo=cutoff_frequency  Zeta=damping_factor  Initialize=off  Vac_Init=[1 45 60]  Vdc_Init=-0.5  PlotResponse=off  param1=[1 500 1]
  A : Outport
  B : Outport  Port=2
  C : Outport  Port=3
  wires:
  a/1 -> 2nd-Order Filter/1
  2nd-Order Filter/1 -> A/1
  b/1 -> 2nd-Order Filter1/1
  2nd-Order Filter1/1 -> B/1
  c/1 -> 2nd-Order Filter2/1
  2nd-Order Filter2/1 -> C/1
